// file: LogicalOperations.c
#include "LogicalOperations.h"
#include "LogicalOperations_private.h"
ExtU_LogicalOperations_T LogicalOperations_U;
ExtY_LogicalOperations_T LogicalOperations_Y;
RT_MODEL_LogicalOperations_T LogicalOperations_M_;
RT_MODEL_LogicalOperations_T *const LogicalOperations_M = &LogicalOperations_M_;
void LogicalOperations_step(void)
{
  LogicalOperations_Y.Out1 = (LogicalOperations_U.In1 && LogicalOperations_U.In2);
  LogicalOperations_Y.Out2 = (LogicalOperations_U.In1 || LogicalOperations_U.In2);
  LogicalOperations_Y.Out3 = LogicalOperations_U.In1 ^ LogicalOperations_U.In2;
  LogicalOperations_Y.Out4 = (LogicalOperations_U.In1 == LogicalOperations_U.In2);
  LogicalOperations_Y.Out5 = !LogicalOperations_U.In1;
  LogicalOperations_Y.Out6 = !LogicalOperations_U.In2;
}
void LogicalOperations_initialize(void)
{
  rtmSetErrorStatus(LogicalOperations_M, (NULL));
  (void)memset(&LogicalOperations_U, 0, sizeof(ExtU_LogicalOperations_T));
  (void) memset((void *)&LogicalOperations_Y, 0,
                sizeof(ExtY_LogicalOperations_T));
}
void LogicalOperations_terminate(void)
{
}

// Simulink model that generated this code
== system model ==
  In1 : Inport
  In2 : Inport
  Out1 : Outport  <- 1: Logic#1
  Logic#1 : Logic  <- 1: In1, 2: In2
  Out2 : Outport  <- 1: Logic#2
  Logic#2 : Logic  Operator=OR  <- 1: In1, 2: In2
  Out3 : Outport  <- 1: Logic#3
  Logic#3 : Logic  Operator=XOR  <- 1: In1, 2: In2
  Out4 : Outport  <- 1: Logic#4
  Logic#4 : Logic  Operator=NXOR  <- 1: In1, 2: In2
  Out5 : Outport  <- 1: Logic#5
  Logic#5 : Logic  Operator=NOT  <- 1: In1
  Out6 : Outport  <- 1: Logic#6
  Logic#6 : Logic  Operator=NOT  <- 1: In2
